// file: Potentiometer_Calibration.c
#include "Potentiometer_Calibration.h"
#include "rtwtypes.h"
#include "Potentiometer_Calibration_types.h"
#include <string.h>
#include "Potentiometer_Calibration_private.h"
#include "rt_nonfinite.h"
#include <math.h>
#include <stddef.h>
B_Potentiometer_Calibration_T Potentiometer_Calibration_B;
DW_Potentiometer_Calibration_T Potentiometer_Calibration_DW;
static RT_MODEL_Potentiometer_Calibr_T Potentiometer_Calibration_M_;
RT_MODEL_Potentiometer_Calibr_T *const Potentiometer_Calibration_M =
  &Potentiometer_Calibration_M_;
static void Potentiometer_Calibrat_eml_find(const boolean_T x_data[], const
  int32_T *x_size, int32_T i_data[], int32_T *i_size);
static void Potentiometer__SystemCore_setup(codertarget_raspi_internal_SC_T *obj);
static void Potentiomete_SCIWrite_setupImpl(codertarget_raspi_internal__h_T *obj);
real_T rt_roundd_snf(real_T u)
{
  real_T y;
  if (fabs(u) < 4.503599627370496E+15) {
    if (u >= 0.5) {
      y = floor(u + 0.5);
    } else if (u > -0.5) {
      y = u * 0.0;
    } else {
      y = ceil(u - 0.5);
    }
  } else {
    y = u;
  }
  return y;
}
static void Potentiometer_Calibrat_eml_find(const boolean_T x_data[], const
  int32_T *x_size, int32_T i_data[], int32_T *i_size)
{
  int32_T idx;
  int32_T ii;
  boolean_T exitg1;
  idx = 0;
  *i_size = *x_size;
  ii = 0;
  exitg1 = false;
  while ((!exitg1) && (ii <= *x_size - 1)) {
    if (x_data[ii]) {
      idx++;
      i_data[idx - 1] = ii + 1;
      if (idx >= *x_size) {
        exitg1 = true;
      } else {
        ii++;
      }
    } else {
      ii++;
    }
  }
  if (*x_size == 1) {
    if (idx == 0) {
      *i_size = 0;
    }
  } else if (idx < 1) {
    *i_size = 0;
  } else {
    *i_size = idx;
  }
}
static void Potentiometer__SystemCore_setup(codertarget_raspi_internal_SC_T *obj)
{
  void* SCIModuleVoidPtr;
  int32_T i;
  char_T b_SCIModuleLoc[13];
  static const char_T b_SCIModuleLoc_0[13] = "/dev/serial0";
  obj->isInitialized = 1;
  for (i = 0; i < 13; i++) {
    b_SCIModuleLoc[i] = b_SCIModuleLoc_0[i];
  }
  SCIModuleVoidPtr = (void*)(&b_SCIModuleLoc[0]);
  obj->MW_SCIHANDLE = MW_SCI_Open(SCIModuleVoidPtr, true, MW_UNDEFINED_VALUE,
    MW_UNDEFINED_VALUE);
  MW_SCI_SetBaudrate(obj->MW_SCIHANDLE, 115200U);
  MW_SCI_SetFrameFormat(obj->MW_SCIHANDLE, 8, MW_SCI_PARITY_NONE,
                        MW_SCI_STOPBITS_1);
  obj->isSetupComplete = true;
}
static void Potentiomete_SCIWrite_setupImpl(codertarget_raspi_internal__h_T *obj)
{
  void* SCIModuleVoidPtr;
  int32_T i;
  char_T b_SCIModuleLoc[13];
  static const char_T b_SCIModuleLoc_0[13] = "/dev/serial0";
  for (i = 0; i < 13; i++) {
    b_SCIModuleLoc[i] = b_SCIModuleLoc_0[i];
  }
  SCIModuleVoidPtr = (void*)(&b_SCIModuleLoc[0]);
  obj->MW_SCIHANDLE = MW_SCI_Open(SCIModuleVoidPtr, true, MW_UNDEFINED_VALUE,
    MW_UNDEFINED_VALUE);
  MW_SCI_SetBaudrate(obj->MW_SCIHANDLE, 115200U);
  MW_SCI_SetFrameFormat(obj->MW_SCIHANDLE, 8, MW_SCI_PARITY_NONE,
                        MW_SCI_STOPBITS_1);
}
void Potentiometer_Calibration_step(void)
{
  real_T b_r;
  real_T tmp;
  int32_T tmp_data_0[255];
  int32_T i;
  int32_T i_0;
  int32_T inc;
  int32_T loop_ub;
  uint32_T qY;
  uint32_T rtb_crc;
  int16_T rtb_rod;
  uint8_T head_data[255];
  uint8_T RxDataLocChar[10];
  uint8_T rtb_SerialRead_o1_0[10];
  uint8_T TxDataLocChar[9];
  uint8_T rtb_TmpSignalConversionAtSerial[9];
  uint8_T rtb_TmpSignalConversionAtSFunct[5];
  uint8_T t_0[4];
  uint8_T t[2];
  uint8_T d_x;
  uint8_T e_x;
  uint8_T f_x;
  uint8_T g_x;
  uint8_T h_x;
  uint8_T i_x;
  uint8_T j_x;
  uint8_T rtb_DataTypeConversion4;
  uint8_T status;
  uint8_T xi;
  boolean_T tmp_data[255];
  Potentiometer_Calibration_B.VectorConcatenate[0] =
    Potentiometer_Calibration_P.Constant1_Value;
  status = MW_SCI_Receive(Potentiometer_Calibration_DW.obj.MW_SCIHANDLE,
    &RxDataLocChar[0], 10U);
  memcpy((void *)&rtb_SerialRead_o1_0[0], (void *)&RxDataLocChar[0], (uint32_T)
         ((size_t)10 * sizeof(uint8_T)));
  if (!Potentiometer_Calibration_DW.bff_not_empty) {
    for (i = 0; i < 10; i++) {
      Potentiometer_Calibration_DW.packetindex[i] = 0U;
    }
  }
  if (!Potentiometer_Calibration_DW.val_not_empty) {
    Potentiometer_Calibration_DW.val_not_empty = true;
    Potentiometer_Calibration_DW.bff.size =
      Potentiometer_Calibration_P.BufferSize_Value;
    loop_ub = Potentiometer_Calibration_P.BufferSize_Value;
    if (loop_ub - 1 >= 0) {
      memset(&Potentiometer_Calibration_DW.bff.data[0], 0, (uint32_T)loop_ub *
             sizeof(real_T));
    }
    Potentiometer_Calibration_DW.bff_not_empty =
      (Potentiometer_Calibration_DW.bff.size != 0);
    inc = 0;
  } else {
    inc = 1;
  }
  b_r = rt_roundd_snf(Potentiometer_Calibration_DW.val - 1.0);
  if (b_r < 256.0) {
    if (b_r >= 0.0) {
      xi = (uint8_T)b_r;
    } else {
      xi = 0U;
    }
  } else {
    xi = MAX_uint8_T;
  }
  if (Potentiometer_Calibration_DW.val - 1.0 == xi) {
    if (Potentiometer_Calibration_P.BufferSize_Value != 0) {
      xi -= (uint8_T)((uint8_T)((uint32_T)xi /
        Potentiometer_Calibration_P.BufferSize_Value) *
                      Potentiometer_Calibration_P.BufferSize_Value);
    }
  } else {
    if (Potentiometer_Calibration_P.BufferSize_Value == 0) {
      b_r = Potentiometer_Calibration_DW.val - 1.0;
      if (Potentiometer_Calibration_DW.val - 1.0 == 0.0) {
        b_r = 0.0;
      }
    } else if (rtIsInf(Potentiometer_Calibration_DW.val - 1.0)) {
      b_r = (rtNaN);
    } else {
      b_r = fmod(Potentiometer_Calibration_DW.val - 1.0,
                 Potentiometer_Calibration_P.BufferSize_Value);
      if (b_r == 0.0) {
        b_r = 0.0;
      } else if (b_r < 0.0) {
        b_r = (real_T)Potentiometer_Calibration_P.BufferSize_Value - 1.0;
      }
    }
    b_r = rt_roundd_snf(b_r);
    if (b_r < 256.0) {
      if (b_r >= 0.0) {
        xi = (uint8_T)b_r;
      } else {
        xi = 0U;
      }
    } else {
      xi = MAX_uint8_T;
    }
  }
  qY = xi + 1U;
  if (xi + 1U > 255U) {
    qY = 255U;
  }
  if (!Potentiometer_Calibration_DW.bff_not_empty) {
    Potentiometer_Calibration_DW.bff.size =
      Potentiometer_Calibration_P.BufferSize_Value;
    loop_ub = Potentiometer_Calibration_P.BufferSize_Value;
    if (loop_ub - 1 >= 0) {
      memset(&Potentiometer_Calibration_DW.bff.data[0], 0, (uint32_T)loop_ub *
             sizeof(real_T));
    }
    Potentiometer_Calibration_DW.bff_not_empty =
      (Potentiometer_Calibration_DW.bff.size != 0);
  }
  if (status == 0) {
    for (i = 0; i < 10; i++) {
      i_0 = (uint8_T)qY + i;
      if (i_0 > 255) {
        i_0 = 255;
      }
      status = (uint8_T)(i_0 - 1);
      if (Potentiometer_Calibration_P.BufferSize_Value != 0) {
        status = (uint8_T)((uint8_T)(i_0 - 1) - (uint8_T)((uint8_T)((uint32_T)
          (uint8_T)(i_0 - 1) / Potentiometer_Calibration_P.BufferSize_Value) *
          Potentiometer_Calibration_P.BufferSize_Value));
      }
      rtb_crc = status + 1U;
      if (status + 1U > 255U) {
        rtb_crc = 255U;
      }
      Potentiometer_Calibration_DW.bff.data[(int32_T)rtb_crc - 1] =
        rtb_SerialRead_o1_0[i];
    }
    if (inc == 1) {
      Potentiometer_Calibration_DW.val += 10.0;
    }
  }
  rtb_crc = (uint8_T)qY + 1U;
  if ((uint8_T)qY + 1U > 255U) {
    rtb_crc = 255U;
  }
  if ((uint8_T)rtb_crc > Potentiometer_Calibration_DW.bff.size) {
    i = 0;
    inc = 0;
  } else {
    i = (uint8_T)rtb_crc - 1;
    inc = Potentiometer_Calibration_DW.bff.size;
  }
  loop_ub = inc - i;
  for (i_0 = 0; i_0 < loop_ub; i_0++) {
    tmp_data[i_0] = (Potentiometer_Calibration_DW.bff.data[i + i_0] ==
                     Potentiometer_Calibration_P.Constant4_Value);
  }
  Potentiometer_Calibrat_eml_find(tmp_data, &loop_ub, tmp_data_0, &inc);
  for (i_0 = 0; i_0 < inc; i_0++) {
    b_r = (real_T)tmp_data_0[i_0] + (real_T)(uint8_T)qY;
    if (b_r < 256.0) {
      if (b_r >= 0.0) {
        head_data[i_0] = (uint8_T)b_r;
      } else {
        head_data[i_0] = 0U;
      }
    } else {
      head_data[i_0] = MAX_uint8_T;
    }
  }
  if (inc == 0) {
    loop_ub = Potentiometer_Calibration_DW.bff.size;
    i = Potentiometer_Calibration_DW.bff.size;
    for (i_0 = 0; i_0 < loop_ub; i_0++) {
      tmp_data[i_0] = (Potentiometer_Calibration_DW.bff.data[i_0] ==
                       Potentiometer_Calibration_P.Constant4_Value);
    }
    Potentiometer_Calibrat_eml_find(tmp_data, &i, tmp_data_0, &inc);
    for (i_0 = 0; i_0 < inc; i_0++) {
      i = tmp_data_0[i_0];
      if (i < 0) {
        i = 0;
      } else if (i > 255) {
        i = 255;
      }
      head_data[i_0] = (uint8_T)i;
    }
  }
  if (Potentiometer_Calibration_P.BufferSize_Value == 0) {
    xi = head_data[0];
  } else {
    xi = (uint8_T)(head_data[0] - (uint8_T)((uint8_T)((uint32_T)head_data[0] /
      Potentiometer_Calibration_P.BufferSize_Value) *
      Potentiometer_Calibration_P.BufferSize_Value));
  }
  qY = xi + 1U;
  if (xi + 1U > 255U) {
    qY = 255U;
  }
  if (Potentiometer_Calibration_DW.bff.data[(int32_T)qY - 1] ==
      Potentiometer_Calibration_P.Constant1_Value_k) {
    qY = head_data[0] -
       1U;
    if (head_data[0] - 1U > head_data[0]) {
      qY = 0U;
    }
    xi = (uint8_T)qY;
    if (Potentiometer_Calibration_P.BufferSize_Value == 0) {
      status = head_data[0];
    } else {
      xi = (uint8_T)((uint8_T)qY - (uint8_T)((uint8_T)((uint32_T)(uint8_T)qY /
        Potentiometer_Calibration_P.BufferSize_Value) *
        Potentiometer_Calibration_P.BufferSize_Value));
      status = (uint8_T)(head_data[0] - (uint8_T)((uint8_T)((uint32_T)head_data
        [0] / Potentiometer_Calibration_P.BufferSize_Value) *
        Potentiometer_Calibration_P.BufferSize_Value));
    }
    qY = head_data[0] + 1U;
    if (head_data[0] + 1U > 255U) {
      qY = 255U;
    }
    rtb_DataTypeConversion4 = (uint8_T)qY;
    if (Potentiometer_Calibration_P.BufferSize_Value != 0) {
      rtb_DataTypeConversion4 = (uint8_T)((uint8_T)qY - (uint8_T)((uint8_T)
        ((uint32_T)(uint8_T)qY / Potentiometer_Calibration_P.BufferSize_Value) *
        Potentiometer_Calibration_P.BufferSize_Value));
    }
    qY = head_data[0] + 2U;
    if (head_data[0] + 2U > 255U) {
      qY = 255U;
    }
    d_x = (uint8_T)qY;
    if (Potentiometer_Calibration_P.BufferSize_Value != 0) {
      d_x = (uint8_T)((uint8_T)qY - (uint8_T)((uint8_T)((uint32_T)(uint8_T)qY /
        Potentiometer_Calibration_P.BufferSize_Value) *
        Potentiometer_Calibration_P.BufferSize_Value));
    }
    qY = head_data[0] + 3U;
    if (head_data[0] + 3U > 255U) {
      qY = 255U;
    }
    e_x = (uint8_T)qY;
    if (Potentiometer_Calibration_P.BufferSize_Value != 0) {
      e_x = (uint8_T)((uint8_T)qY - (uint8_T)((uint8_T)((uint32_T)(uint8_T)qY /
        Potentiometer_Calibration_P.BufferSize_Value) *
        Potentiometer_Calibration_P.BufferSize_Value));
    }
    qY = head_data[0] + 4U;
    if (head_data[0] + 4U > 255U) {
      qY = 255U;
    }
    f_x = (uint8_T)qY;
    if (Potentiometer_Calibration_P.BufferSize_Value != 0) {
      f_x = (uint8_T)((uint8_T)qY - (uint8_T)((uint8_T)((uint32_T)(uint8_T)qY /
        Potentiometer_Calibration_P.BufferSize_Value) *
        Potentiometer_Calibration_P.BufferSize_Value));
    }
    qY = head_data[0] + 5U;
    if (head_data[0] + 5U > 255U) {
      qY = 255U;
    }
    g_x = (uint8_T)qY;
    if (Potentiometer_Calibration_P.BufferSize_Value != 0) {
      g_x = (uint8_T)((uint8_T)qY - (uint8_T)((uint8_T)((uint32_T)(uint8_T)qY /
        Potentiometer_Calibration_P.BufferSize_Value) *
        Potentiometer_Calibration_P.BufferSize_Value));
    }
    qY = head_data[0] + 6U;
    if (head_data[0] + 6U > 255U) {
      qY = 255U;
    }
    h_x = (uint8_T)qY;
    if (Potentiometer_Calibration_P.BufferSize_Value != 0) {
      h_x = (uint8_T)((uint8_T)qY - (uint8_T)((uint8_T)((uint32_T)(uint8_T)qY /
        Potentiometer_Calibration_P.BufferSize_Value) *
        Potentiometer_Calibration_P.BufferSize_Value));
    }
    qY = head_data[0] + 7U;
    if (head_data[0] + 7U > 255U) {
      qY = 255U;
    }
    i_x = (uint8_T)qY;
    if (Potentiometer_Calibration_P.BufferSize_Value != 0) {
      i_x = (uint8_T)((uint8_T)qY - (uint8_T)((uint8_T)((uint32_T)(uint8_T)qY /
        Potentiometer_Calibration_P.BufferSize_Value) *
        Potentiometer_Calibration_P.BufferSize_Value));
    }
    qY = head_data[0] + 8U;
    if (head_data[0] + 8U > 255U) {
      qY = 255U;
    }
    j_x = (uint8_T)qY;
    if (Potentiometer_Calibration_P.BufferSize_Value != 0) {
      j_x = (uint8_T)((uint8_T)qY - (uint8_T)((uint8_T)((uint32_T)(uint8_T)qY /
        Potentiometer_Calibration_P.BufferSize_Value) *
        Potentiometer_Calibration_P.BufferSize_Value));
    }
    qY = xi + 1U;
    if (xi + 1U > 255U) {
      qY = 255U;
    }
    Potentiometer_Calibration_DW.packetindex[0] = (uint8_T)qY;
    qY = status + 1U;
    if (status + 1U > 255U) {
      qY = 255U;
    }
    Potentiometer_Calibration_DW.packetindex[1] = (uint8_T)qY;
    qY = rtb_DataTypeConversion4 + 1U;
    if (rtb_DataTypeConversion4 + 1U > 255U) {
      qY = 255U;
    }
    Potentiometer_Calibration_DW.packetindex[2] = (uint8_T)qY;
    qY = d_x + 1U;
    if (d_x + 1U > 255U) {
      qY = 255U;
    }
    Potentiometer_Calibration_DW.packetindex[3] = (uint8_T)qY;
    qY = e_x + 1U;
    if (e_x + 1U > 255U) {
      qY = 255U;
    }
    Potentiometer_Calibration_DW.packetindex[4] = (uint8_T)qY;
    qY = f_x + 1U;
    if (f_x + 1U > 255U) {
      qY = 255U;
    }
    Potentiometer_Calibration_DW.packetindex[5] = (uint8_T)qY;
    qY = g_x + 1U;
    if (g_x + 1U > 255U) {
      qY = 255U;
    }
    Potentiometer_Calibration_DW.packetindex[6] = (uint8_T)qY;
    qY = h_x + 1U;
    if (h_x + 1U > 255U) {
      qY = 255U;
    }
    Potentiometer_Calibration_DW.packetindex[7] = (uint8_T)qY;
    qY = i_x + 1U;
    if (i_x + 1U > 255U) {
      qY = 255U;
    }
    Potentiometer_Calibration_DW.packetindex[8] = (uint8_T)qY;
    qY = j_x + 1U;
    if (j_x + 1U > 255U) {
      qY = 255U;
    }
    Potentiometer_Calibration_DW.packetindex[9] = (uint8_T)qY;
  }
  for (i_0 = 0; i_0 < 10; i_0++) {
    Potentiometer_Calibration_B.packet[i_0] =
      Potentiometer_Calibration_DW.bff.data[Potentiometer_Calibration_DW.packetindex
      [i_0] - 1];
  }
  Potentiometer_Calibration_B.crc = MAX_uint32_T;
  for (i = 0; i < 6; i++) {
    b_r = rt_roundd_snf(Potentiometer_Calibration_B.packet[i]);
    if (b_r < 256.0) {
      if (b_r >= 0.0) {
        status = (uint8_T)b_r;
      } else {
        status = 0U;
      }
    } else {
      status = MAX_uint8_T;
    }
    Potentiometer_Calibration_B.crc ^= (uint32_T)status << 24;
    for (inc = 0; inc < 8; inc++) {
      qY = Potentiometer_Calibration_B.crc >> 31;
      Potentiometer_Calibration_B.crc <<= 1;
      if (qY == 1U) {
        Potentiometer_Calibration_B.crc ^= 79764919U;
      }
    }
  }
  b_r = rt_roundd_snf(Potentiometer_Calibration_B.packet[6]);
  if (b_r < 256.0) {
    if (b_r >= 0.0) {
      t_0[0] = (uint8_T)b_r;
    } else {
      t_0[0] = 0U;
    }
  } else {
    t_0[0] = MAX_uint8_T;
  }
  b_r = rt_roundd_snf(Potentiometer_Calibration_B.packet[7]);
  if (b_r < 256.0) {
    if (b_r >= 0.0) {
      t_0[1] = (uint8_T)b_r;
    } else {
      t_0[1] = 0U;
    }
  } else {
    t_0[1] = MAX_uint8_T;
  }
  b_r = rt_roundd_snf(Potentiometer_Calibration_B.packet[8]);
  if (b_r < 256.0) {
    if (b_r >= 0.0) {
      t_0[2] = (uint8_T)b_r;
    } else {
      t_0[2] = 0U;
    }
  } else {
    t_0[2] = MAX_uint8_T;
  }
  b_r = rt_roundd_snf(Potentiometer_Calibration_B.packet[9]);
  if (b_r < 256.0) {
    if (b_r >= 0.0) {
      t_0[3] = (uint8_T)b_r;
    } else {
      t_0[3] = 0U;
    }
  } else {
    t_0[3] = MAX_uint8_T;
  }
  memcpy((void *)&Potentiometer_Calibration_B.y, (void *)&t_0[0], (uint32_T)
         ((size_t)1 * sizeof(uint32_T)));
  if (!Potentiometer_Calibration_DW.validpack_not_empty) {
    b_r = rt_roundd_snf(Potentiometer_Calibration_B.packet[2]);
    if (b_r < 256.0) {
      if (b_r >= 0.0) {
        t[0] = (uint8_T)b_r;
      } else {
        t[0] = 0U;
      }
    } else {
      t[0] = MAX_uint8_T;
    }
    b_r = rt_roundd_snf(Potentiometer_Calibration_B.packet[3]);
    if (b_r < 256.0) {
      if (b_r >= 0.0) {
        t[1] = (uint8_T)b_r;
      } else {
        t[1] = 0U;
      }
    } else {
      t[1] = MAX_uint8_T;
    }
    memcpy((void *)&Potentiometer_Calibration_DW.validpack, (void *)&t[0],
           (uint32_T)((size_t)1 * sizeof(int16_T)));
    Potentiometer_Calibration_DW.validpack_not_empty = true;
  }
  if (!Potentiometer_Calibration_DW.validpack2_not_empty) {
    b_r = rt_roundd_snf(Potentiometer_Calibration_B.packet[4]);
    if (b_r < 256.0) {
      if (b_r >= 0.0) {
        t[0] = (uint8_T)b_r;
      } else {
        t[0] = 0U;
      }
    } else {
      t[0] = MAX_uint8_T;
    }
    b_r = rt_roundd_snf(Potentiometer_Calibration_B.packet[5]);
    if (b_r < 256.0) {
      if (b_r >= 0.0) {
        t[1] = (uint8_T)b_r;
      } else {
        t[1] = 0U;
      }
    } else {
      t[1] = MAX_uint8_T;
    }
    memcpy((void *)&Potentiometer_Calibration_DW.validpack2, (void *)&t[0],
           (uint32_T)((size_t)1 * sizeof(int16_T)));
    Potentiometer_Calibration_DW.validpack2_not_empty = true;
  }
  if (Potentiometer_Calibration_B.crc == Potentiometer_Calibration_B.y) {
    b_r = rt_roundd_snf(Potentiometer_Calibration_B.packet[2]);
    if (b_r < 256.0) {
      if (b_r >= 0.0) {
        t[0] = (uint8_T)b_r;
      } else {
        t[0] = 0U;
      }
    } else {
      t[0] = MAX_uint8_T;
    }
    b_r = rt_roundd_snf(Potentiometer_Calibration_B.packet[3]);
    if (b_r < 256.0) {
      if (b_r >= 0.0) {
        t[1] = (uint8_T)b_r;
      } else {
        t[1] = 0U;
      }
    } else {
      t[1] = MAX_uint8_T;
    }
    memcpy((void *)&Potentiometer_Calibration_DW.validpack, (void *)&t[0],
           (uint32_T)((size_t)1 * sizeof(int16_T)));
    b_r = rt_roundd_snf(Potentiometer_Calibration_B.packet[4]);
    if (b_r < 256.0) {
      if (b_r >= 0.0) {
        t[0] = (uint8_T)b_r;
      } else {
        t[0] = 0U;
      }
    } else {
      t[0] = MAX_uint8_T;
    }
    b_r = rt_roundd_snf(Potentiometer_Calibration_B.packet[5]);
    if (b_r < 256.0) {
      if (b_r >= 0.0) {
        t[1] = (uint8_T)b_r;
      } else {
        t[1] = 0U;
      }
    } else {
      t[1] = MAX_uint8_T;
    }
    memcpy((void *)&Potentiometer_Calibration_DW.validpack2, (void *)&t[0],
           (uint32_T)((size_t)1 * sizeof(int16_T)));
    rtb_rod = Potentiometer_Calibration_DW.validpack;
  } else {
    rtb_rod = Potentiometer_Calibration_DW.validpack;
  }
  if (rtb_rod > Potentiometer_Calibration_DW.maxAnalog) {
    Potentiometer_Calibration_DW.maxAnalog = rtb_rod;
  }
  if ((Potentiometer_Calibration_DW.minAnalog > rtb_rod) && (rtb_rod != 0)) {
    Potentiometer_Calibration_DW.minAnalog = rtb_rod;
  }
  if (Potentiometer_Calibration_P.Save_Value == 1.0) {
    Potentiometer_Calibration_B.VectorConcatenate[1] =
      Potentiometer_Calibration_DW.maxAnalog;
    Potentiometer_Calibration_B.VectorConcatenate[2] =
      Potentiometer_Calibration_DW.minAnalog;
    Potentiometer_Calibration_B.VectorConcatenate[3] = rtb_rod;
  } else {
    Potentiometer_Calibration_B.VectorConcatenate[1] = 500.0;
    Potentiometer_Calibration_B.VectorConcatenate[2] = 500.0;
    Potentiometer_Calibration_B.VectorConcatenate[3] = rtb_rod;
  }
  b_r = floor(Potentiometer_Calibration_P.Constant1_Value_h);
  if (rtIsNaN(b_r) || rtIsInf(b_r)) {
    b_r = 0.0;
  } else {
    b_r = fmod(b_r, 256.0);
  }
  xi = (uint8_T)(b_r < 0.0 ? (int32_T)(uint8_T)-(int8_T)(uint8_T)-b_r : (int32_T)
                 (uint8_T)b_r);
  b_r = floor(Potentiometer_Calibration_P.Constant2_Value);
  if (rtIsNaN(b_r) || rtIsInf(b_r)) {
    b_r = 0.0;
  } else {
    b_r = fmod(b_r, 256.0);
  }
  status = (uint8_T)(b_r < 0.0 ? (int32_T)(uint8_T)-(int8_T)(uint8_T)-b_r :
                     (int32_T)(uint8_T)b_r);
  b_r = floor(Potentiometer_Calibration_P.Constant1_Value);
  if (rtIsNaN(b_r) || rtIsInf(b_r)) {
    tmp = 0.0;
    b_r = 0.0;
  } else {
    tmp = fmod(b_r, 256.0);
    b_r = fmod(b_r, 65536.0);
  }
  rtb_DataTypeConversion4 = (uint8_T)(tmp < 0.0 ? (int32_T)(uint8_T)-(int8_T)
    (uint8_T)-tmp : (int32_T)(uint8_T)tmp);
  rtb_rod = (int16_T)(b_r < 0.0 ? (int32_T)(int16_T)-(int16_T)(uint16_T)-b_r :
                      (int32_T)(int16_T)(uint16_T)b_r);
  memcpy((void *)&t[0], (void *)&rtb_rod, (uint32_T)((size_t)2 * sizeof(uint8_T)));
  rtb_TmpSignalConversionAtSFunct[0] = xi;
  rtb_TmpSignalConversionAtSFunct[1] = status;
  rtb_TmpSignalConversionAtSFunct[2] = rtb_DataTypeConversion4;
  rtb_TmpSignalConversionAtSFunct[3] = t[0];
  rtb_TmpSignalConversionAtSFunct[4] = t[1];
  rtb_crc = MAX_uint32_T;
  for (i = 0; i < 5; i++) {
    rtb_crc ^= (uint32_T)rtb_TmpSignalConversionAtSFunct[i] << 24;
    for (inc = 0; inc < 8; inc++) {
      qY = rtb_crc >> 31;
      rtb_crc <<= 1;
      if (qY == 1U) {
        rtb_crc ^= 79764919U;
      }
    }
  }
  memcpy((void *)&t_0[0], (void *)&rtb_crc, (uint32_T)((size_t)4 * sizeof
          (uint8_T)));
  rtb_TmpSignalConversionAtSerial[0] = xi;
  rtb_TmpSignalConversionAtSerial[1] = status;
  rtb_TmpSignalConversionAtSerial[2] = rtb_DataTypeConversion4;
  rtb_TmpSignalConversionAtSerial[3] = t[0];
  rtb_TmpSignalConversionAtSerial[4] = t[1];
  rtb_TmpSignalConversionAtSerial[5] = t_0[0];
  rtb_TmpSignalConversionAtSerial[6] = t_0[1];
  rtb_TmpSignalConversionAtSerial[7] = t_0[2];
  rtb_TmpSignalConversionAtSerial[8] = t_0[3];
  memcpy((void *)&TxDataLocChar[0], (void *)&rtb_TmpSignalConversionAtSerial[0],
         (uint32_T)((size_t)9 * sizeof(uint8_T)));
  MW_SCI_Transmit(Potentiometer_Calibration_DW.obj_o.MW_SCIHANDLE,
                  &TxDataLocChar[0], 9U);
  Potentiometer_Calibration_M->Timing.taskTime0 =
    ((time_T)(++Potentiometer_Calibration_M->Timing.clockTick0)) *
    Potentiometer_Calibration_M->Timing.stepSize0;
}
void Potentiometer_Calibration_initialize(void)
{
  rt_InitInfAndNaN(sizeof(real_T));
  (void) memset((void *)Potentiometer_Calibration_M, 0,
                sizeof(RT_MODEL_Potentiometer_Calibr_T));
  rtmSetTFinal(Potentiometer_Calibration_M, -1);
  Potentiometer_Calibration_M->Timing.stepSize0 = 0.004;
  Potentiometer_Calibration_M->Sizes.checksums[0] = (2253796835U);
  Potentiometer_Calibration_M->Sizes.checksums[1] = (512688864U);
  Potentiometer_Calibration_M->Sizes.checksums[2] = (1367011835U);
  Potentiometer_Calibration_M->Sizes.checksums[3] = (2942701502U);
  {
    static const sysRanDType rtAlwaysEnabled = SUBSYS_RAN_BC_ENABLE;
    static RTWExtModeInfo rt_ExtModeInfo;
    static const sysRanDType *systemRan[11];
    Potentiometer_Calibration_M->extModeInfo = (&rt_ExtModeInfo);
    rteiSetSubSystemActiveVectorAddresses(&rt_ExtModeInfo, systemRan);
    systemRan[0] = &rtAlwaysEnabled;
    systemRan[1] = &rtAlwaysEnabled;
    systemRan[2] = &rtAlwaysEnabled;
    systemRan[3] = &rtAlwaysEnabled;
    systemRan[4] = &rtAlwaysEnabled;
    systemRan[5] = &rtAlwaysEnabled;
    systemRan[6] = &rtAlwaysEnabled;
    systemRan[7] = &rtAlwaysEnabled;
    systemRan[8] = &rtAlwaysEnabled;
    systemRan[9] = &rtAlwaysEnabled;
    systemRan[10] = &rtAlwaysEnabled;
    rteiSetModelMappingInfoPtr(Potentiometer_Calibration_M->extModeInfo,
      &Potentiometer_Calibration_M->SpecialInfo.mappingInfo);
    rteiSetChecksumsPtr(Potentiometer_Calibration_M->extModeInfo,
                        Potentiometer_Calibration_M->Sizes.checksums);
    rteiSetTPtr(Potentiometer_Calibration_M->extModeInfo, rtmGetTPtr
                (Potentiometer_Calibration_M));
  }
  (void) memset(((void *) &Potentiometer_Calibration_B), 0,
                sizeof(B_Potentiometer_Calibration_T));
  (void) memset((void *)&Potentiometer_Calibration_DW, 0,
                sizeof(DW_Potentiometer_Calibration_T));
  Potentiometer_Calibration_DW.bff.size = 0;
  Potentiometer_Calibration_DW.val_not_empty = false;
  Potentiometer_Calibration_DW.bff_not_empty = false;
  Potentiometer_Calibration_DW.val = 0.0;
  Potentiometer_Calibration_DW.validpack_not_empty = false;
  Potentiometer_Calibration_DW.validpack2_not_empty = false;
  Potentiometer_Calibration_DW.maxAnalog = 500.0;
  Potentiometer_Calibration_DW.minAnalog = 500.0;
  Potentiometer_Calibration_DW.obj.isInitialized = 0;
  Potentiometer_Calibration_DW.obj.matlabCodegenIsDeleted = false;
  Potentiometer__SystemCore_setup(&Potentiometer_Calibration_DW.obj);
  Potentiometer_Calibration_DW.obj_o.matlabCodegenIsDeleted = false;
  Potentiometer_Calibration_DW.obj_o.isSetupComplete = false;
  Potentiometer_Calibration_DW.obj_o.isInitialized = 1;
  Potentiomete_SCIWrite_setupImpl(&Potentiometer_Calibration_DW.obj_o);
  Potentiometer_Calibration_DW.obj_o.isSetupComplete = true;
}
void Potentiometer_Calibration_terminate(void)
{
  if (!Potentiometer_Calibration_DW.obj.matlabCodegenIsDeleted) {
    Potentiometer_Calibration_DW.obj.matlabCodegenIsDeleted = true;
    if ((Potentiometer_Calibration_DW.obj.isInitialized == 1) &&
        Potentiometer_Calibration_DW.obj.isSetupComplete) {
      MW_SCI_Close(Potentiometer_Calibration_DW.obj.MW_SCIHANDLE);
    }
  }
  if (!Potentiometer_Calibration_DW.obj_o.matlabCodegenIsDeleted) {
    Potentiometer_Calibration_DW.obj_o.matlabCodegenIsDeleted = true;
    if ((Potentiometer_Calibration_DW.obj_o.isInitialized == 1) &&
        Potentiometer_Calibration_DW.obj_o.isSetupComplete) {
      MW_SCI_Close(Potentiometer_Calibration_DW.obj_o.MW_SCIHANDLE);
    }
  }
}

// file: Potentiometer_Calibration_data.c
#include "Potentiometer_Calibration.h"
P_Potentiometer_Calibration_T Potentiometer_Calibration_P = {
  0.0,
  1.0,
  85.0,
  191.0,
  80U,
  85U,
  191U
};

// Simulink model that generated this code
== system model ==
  SerialWrite#1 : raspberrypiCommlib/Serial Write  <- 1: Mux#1
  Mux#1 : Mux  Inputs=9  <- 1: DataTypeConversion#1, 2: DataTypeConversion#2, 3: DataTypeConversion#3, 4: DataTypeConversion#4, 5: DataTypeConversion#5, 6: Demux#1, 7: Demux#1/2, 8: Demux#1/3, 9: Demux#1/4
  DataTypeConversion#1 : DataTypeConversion  <- 1: Constant1
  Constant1 : Constant  Value=85
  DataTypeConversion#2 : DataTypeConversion  <- 1: Constant2
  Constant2 : Constant  Value=191
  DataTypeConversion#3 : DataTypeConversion  <- 1: DataTypeConversion4
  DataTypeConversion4 : DataTypeConversion  <- 1: Constant#1
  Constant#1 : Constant  Value=0
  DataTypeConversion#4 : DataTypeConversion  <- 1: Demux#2
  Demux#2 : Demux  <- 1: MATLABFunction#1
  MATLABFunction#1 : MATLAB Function  <- 1: DataTypeConversion#6
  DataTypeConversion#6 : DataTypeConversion  <- 1: Constant#1
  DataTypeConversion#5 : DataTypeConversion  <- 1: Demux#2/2
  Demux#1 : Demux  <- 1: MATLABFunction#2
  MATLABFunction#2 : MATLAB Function  <- 1: MATLABFunction#3
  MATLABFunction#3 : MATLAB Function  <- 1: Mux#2
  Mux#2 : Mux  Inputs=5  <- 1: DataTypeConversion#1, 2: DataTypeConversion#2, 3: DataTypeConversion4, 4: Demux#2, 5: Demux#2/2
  VectorConcatenate : Concatenate  <- 1: Constant#1, 2: MATLABFunction#4, 3: MATLABFunction#4/2, 4: MATLABFunction#4/3
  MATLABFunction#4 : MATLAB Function  <- 1: DataTypeConversion#7, 2: Save
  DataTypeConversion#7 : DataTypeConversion  <- 1: DataTypeConversion#8
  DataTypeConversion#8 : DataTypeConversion  <- 1: MATLABFunction#5
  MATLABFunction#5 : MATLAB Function  <- 1: MATLABFunction#6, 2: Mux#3, 3: MATLABFunction#7
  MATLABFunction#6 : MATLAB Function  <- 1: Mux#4
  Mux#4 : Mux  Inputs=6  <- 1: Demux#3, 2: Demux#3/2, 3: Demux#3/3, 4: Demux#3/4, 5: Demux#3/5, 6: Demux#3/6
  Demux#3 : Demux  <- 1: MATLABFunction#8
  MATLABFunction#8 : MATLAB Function  <- 1: BufferSize, 2: SerialRead, 3: SerialRead/2, 4: Constant4, 5: Constant#2
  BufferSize : Constant  Value=80
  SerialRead : raspberrypiCommlib/Serial Read
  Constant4 : Constant  Value=85
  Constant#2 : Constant  Value=191
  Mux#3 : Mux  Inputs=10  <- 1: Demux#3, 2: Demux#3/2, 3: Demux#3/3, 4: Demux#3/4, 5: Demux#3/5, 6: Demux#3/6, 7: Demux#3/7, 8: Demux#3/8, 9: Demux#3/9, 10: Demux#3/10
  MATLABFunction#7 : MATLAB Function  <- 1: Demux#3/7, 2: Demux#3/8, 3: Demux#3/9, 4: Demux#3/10
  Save : Constant
== matlab function MATLAB Function ==
function [maxValue,minValue,initialValue] = fcn(Analog,Save)
    persistent maxAnalog
    if isempty(maxAnalog)
        maxAnalog=500;
    end
    persistent minAnalog
    if isempty(minAnalog)
        minAnalog=500;
    end
    if (Analog>maxAnalog)
        maxAnalog=Analog;
    end
    if (minAnalog > Analog)
        if (Analog  ~= 0)
            minAnalog=Analog;
        end
    end
    if (Save==1)
        maxValue=maxAnalog;
        minValue=minAnalog;
        initialValue=Analog;
    else
        maxValue=500;
        minValue=500;
        initialValue=Analog;
    end
end

== matlab function MATLAB Function ==
function crc = crc_32(data)

% Computes the CRC-32/MPEG-2 checksum value of a byte vector.
% Uses a left shifting (not reflected) CRC along with the 
% CRC polynomial 0x04C11DB7 and initial CRC value of 0xFFFFFFFF,
% and is not post complemented.
%--------------------------------------------------------------------------
%   Version:    130
%   Programmer: Oliver Calderbank
%   Date:       21-07-2019

% Initialize variables
crc  = uint32(hex2dec('FFFFFFFF'));
poly = uint32(hex2dec('04C11DB7'));
data = uint8(data);
temp = uint32(data);

for i = 1:length(data)
    % xor next byte to upper bits of crc
    crc = bitxor(crc,uint32(bitshift(temp(i),24)));
    for j = 1:8
        msb = bitsra(crc,31);
        crc = bitsll(crc,1);
        if msb == 1 
            crc = bitxor(crc,poly);
        end 
    end
end
end

== matlab function MATLABFunction#1 ==
function y = fcn(u)
t=typecast(int16(u),'uint8');
y = [t(1) t(2)];

== matlab function MATLABFunction#2 ==
function y = fcn(u)
t=typecast(uint32(u),'uint8');
y = [t(1) t(2) t(3) t(4)];

== matlab function MATLABFunction#8 ==
function packet   = fcn(bufSize,newval,status,headval,head2val)
%initializing
persistent val;
persistent bff;
persistent packetindex
if isempty(bff)
    packetindex =uint8(zeros(1,10));
end
if isempty(val)
    val=0;
    bff = zeros(bufSize,1); %initializing
    inc=0;
else
    inc=1;
end

ind =uint8( mod(val-1,bufSize) + 1); %current index
if isempty(bff)
    bff = zeros(bufSize,1); %initializing
end
if status==0  %UART Status
    for i = 1:1:10
        bff(mod(ind-1+i-1,bufSize)+1) = newval(i); %adding the circular buffer
    end
    if inc==1
        val=val+10;   
    end
end
if ind==0
    val=0;
end
buffout =uint8( bff((1:80)));  % whole buffer
head=uint8(find(bff(ind+1:end)==headval)+double(ind)); %finding first header
if isempty(head)
    head=uint8(find(bff(1:end)==headval));
end
if bff(mod(head(1),bufSize)+1)==head2val %header2 check
    packetindex=[mod(head(1)-1,bufSize)+1 mod(head(1),bufSize)+1 mod(head(1)+1,bufSize)+1 mod(head(1)+2,bufSize)+1 ... %adding correct package's index to array
                 mod(head(1)+3,bufSize)+1 mod(head(1)+4,bufSize)+1 mod(head(1)+5,bufSize)+1 mod(head(1)+6,bufSize)+1 mod(head(1)+7,bufSize)+1 mod(head(1)+8,bufSize)+1];
end
lastadd=uint8(bff(head(1)+1));
packet=bff(packetindex);

== matlab function MATLABFunction#6 ==
function crc = crc_32(data)

% Computes the CRC-32/MPEG-2 checksum value of a byte vector.
% Uses a left shifting (not reflected) CRC along with the 
% CRC polynomial 0x04C11DB7 and initial CRC value of 0xFFFFFFFF,
% and is not post complemented.
%--------------------------------------------------------------------------
%   Version:    130
%   Programmer: Oliver Calderbank
%   Date:       21-07-2019

% Initialize variables
crc  = uint32(hex2dec('FFFFFFFF'));
poly = uint32(hex2dec('04C11DB7'));
data = uint8(data);
temp = uint32(data);

for i = 1:length(data)
    % xor next byte to upper bits of crc
    crc = bitxor(crc,uint32(bitshift(temp(i),24)));
    for j = 1:8
        msb = bitsra(crc,31);
        crc = bitsll(crc,1);
        if msb == 1 
            crc = bitxor(crc,poly);
        end 
    end
end
end

== matlab function MATLABFunction#5 ==
function [rod,cart] = fcn(calc,packet,recv)
persistent validpack;
persistent validpack2;
if isempty(validpack)
    Axisx=[packet(3) packet(4)];
    validpack=typecast(uint8(Axisx),'int16');
end
if isempty(validpack2)
    Axisy=[packet(5) packet(6)];
    validpack2=typecast(uint8(Axisy),'int16');
end
if calc==recv
    Axisx=[packet(3) packet(4)];
    validpack=typecast(uint8(Axisx),'int16');
    Axisy=[packet(5) packet(6)];
    validpack2=typecast(uint8(Axisy),'int16');
    rod=validpack;
    cart=validpack2;
else
	rod=validpack;
    cart=validpack2;
end

== matlab function MATLABFunction#7 ==
function y = fcn(u,v,z,t)
x=[u v z t];
k=typecast(uint8(x),'uint32');
y = k;
